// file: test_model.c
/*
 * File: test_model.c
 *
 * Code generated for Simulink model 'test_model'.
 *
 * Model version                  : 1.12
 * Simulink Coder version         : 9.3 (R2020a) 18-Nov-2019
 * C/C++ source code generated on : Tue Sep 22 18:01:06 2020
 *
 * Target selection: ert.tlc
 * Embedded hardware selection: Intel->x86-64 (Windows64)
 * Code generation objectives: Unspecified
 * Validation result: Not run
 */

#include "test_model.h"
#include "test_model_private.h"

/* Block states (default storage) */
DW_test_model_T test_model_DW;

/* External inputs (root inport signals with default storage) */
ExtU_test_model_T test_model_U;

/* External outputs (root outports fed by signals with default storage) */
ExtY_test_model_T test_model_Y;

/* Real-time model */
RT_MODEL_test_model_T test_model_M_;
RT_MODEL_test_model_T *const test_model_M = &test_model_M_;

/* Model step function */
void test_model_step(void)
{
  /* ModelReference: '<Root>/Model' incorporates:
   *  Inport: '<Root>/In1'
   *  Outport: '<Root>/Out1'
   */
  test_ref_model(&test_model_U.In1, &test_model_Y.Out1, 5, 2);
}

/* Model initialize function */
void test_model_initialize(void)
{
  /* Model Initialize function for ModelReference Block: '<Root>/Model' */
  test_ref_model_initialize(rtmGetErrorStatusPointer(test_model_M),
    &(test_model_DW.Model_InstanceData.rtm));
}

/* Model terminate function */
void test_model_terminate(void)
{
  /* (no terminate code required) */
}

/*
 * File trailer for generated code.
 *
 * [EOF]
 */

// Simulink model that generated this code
simulink model "test_model"  (R2020a)
settings: Solver=FixedStepDiscrete  StartTime=0.0  StopTime=10.0  FixedStep=0.01  RelTol=1e-3
undefined symbols (not defined in the file): a, b

== system test_model ==
  In1 : Inport
  Model : ModelReference  ModelNameDialog=test_ref_model.slx  ParameterArgumentNames=a,b  ParameterArgumentValues=5,2  UsingDefaultArgumentValue=0,0  SimulationMode=Normal  ModelReferenceVersion=1.9
  Out1 : Outport
  wires:
  In1/1 -> Model/1
  Model/1 -> Out1/1
